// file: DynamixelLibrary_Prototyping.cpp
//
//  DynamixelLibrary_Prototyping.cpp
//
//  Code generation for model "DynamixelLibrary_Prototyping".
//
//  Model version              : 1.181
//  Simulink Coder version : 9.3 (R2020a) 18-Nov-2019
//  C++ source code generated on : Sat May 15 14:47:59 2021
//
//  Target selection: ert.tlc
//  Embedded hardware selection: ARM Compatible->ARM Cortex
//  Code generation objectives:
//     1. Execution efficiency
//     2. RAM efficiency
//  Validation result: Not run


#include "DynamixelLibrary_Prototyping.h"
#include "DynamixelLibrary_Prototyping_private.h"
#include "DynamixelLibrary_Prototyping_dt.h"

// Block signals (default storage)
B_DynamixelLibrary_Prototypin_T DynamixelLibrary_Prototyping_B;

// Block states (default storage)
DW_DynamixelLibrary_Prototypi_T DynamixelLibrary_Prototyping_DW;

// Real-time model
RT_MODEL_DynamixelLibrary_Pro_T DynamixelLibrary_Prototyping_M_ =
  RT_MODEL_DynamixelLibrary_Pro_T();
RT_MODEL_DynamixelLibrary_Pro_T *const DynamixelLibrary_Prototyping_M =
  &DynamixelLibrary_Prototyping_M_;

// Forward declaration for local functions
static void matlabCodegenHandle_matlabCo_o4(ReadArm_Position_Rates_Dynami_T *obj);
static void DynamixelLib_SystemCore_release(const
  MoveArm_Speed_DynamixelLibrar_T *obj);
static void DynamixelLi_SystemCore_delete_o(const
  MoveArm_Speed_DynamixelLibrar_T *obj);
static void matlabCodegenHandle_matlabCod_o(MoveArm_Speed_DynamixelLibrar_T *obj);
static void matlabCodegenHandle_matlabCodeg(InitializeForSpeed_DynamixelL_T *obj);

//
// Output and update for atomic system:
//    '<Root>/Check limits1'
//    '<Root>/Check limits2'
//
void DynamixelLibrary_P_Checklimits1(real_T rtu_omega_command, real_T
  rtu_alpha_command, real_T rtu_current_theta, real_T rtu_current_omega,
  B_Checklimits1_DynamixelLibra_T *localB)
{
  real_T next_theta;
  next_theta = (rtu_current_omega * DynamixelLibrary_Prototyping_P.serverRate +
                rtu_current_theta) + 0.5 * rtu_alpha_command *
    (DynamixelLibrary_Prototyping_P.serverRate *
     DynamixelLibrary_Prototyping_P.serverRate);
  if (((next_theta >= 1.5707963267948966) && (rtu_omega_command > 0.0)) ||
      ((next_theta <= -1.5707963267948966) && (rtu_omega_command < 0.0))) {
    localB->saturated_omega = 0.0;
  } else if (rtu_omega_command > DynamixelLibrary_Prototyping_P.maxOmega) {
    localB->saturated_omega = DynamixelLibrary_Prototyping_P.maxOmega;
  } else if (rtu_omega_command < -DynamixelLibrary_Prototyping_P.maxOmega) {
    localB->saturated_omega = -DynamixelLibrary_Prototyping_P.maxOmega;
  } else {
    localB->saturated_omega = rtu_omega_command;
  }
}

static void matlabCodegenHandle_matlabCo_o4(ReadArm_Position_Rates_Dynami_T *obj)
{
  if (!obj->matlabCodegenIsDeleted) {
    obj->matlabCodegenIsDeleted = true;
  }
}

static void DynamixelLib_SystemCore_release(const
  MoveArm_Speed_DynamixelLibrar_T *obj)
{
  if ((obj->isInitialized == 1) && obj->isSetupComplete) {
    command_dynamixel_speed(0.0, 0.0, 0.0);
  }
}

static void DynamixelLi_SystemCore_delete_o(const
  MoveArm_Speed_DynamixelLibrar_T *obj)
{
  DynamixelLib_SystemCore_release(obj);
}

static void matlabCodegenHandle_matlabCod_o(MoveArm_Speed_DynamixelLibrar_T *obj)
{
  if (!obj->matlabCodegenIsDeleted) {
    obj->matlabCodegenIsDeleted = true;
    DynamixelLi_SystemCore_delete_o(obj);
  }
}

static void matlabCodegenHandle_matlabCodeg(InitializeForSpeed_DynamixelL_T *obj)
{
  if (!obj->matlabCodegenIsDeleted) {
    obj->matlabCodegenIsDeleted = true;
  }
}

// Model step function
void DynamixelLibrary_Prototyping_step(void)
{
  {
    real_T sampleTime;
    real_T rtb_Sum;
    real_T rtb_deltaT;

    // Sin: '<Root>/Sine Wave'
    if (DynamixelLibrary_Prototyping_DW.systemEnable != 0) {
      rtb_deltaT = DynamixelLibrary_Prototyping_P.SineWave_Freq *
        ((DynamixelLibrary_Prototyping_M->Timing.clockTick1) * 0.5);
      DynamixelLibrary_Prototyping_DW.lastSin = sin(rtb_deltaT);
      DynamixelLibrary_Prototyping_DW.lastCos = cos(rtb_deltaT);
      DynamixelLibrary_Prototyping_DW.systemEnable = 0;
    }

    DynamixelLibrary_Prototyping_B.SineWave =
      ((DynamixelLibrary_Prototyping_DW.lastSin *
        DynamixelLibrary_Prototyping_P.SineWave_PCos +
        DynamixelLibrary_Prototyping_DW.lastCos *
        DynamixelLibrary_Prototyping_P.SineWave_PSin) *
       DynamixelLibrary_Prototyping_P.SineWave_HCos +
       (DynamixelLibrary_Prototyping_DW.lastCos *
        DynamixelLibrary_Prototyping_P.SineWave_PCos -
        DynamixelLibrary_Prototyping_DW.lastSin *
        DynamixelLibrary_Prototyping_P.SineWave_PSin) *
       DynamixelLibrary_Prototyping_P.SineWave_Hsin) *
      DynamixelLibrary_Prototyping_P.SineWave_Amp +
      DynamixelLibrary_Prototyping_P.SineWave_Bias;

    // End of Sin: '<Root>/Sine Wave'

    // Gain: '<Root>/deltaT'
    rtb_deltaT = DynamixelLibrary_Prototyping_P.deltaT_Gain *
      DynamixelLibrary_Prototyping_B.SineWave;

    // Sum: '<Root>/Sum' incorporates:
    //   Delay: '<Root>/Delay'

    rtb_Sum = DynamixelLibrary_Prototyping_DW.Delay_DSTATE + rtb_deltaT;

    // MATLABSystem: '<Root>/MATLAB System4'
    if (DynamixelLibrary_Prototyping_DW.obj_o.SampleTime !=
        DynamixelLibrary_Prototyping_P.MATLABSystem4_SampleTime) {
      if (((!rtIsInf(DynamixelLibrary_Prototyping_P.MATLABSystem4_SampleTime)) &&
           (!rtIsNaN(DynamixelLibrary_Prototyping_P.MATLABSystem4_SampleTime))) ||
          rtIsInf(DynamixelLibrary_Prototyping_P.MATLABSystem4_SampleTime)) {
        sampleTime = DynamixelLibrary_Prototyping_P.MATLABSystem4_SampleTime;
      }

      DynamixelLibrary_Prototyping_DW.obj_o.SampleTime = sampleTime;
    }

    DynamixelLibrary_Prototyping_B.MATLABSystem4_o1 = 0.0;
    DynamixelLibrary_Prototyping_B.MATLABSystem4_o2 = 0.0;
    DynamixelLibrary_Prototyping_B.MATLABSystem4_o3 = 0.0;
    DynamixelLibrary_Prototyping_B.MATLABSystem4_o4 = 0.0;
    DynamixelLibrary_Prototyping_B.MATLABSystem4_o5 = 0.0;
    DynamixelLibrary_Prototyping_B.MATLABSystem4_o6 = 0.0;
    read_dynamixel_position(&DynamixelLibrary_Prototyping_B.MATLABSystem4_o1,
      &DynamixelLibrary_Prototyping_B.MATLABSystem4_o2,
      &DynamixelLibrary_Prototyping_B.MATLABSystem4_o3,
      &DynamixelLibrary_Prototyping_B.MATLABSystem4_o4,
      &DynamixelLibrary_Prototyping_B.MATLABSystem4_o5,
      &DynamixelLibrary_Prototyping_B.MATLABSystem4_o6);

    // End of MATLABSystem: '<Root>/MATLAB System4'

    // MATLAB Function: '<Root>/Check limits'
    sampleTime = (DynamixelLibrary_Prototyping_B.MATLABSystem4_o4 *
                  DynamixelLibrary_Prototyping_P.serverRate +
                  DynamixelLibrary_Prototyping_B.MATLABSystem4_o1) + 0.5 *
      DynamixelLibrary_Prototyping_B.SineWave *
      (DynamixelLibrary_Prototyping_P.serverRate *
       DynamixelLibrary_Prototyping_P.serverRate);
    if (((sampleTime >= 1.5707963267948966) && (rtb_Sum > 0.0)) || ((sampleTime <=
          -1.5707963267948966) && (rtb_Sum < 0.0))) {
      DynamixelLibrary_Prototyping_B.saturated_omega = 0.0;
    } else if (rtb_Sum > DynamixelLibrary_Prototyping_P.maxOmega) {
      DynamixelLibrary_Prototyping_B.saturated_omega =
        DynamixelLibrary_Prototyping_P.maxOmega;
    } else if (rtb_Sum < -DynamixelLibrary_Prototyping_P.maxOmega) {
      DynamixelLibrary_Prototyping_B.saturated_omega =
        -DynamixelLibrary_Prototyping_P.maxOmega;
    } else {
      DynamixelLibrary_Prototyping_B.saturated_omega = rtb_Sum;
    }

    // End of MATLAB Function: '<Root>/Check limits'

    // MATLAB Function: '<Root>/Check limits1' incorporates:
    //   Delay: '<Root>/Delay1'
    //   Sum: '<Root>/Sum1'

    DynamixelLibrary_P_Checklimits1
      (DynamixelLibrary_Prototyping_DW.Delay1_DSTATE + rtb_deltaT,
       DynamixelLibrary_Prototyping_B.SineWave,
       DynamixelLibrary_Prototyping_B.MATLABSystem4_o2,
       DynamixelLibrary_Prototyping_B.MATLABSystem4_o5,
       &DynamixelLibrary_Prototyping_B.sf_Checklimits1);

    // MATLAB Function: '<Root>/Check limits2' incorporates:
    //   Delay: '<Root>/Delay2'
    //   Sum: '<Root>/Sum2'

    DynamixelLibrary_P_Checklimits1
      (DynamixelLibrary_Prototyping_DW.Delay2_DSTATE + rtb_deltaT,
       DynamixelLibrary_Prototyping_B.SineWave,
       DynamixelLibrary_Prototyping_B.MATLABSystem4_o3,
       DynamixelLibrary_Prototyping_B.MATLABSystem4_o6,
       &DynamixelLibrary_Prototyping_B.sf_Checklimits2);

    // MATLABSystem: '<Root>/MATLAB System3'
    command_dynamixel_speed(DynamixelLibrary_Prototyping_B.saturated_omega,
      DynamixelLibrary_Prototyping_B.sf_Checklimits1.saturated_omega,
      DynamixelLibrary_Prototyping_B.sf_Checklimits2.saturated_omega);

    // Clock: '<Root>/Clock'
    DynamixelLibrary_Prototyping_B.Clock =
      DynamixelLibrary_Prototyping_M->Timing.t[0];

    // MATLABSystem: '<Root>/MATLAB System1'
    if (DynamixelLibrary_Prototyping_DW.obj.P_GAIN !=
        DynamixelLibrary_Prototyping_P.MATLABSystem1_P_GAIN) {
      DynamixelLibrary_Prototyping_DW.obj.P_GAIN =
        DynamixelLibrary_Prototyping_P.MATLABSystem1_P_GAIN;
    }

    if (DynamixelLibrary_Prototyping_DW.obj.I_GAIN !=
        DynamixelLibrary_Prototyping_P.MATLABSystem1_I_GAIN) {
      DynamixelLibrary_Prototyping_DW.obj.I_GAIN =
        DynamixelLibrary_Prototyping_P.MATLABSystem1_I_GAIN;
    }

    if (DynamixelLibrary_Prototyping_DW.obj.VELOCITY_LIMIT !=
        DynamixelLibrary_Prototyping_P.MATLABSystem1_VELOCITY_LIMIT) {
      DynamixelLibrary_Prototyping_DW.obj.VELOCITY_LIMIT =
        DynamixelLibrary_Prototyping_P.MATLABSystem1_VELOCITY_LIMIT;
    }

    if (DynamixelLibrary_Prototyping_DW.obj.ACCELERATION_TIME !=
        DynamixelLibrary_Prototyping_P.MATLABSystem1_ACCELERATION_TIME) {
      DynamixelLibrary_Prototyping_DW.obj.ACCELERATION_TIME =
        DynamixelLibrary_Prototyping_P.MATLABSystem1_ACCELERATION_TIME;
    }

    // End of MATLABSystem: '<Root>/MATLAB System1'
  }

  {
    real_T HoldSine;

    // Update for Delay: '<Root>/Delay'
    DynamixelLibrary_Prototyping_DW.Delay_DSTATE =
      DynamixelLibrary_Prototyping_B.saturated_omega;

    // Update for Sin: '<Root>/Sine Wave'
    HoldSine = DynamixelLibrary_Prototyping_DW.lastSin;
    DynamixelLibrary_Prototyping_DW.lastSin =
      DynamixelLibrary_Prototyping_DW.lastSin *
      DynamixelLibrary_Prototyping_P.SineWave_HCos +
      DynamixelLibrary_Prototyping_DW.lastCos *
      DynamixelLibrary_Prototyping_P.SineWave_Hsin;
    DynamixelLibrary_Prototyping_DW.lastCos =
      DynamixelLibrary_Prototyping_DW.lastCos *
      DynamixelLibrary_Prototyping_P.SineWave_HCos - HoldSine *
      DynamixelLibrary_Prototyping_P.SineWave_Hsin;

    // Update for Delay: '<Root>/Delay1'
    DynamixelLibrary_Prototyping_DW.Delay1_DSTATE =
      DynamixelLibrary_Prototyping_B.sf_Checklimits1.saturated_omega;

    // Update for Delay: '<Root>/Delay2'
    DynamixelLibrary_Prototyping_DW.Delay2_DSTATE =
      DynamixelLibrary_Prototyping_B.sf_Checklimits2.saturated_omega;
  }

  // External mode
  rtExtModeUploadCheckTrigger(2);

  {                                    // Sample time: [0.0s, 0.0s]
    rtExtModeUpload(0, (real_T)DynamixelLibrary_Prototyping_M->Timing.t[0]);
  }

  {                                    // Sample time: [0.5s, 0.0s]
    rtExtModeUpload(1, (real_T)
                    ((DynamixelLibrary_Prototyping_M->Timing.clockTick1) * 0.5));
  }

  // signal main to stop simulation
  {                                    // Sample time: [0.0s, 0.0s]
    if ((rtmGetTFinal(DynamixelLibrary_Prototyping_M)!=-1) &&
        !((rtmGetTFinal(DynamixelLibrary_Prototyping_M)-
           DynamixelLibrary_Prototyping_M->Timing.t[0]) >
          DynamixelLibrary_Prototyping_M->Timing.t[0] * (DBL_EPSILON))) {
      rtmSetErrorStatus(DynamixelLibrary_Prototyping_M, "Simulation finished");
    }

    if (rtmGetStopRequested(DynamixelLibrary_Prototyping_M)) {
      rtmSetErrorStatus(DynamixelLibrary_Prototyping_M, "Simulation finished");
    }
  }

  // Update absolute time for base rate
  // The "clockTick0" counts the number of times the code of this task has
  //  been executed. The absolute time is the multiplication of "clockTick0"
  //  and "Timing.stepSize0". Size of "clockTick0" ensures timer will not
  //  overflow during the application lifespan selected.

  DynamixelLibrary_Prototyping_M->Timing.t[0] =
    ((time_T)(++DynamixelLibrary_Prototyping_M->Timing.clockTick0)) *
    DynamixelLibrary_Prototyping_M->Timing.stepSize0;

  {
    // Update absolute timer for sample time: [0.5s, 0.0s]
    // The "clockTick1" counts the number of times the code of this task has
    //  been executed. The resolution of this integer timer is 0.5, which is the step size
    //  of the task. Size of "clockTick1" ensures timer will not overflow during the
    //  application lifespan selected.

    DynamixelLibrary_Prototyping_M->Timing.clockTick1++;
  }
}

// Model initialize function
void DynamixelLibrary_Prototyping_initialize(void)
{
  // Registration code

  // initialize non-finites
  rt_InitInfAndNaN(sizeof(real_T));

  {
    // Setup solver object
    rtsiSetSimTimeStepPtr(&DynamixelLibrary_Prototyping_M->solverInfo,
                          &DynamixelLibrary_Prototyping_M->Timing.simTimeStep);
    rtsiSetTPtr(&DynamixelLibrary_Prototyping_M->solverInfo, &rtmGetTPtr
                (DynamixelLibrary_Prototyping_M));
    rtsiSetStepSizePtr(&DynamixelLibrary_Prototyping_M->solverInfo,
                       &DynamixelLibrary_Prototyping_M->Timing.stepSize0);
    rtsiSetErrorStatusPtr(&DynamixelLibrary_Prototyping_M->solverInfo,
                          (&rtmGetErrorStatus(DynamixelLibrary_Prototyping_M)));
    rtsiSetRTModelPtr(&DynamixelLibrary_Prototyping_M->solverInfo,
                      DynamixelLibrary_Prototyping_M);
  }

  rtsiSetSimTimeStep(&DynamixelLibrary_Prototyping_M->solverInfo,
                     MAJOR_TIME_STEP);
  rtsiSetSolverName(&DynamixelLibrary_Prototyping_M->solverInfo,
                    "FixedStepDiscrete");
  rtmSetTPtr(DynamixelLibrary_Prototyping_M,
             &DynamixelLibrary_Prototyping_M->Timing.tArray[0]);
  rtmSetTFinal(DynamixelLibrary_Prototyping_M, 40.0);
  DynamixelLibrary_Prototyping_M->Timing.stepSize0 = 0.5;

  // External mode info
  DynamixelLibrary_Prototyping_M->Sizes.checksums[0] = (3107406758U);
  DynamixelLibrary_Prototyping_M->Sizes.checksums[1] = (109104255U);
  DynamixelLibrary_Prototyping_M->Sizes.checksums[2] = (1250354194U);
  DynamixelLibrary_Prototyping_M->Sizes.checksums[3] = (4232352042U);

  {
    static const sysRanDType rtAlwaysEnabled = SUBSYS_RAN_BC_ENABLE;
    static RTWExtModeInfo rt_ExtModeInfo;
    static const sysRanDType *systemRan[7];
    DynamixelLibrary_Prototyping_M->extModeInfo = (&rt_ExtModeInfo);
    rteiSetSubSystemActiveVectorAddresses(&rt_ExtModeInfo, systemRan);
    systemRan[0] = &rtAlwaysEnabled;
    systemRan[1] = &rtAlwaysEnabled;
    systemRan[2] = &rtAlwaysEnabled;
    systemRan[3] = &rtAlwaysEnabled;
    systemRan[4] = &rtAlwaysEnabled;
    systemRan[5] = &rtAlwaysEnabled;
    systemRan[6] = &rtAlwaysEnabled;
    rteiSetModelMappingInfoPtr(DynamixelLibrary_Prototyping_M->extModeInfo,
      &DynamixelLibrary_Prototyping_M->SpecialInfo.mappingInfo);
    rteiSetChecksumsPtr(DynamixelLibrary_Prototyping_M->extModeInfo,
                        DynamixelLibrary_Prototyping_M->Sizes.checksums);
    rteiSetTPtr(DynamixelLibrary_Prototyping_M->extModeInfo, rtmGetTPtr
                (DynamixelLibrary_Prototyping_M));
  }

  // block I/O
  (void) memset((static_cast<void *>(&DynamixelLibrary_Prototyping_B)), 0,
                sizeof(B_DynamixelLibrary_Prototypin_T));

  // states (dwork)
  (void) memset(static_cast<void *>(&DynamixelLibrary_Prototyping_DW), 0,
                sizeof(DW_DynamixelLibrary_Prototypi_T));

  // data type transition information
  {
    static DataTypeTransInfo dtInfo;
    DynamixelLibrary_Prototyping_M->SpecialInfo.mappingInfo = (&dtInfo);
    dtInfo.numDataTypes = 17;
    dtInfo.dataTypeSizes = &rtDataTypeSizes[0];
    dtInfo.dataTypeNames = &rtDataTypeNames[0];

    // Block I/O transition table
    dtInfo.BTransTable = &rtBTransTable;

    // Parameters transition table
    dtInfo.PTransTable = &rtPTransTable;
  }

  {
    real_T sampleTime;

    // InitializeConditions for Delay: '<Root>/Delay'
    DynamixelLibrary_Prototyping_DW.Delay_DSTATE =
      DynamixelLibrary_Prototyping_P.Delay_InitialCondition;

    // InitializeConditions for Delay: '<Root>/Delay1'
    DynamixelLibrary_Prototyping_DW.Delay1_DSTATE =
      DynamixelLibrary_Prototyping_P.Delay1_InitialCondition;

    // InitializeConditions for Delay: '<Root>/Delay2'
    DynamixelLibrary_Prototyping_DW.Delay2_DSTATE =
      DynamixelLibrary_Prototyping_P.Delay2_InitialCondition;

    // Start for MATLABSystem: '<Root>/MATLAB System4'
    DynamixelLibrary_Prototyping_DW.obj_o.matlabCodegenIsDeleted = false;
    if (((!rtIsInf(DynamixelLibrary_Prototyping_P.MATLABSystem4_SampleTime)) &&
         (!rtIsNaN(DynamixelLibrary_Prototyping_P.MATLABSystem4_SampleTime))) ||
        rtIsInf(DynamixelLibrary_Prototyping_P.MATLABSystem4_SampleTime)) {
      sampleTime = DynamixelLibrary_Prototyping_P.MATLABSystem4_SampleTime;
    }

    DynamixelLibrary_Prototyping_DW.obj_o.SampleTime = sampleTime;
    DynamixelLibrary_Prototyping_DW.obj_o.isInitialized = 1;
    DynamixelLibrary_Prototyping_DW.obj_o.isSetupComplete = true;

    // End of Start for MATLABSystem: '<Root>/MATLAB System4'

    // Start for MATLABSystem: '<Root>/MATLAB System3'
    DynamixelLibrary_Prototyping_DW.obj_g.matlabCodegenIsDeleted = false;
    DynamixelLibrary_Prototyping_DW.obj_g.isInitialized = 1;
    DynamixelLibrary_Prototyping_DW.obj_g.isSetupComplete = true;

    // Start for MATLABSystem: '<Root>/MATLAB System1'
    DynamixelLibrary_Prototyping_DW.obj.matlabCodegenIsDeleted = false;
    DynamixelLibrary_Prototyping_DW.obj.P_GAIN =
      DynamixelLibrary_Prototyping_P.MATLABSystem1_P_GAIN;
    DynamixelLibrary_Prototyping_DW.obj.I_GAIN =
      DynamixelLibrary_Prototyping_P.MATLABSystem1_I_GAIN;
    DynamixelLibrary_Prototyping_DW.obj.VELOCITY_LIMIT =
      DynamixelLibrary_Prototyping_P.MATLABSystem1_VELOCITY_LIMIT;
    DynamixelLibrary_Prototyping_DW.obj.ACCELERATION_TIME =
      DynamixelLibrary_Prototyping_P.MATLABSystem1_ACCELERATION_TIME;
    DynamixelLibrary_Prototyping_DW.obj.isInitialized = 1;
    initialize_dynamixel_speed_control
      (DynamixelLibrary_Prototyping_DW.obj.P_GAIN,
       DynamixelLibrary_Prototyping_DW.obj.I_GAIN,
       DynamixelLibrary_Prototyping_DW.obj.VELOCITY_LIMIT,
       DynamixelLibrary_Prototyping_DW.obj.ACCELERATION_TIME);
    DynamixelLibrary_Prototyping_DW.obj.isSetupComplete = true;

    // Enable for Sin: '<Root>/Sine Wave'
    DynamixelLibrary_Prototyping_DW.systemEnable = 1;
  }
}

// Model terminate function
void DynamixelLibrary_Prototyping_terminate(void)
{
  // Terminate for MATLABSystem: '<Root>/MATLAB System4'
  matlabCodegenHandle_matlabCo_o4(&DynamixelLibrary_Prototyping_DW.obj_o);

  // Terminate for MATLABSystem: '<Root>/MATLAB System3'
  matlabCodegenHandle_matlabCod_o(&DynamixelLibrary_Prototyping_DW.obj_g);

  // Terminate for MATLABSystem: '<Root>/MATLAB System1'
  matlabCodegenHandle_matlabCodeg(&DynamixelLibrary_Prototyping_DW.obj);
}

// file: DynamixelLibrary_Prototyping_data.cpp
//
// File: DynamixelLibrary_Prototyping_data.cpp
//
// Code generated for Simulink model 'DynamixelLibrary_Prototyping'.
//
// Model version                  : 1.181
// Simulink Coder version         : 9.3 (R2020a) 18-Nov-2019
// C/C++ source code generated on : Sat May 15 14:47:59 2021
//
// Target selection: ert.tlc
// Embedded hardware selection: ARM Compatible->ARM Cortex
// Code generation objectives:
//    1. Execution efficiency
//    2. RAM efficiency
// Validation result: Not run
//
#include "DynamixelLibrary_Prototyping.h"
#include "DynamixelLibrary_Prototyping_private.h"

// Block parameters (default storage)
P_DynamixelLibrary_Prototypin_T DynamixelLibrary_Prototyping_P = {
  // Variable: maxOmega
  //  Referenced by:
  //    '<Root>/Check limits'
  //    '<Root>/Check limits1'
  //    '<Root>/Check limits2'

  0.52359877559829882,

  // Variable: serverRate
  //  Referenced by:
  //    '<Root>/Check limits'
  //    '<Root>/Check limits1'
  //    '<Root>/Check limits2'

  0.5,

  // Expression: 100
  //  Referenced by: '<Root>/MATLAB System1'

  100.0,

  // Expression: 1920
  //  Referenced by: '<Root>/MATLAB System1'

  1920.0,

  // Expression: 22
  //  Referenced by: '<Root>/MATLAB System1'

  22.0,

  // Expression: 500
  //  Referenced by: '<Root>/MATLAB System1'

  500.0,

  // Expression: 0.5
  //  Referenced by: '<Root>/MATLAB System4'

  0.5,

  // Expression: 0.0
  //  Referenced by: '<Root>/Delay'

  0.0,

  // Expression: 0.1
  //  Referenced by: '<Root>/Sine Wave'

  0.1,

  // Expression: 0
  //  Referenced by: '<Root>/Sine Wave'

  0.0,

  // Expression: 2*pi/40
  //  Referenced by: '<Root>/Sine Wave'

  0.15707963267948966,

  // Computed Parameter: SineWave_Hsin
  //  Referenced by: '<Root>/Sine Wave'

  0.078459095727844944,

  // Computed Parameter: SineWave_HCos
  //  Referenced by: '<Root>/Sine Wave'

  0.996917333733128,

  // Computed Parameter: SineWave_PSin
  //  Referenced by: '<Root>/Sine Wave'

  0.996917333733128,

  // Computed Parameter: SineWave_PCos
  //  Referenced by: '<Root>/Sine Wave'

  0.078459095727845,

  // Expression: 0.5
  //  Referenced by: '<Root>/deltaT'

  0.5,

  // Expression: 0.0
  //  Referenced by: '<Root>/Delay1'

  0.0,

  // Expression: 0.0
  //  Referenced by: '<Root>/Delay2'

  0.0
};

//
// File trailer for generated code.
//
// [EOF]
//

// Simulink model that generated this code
simulink model "DynamixelLibrary_Prototyping"  (R2020a)
settings: Solver=FixedStepAuto  StartTime=0.0  StopTime=40  FixedStep=0.5  RelTol=1e-3  EnableMultiTasking=on
values from neighbouring files (symbols this model uses):
  serverRate = 1/10    (= 0.1)    [Run_Initializer.m]
undefined symbols (not defined in the file or in its folder): maxOmega

== system DynamixelLibrary_Prototyping ==
  note: check if this angular rate will lead to joint limits being reached
  note: omega_t = omega_t-1 + alpha*deltaT
  Check limits : MATLAB Function  TreatAsAtomicUnit=on
  Check limits1 : MATLAB Function  TreatAsAtomicUnit=on
  Check limits2 : MATLAB Function  TreatAsAtomicUnit=on
  Clock : Clock
  Constant : Constant  Commented=on  Value=0
  Constant2 : Constant  Commented=on  Value=50
  Delay : Delay  DelayLength=1
  Delay1 : Delay  DelayLength=1
  Delay2 : Delay  DelayLength=1
  MATLAB System : MATLABSystem  Commented=on  System=InitializeForPosition  P_GAIN=400  I_GAIN=0  D_GAIN=200  MAX_POSITION=3072  MIN_POSITION=1024  VELOCITY_PROFILE=0  ACCELERATION_PROFILE=0
  MATLAB System1 : MATLABSystem  System=InitializeForSpeed  P_GAIN=100  I_GAIN=1920  VELOCITY_LIMIT=22  ACCELERATION_TIME=500
  MATLAB System10 : MATLABSystem  Commented=on  System=InitializeForSpecial  CURRENT_LIMIT=850  P_GAIN=400  I_GAIN=0  D_GAIN=200  MAX_POSITION=3072  MIN_POSITION=1024  VELOCITY_LIMIT=0
  MATLAB System11 : MATLABSystem  Commented=on  System=MoveArm_Special
  MATLAB System12 : MATLABSystem  Commented=on  System=InitializeForArmGripper  P_GAIN_ARM=400  I_GAIN_ARM=0  D_GAIN_ARM=200  P_GAIN_PROX=400  I_GAIN_PROX=0  D_GAIN_PROX=200  P_GAIN_DIST=400  I_GAIN_DIST=0  D_GAIN_DIST=200  MAX_POSITION_ARM=3072  MIN_POSITION_ARM=1024  MAX_POSITION_PROX=3072  MIN_POSITION_PROX=1024  MAX_POSITION_DIST=3072  MIN_POSITION_DIST=1024  VELOCITY_LIMIT_ARM=0  VELOCITY_LIMIT_GRIP=0  MAX_CURRENT_GRIP=1000
  MATLAB System13 : MATLABSystem  Commented=on  System=MoveArmGripper_Position
  MATLAB System2 : MATLABSystem  Commented=on  System=MoveArm_Position
  MATLAB System3 : MATLABSystem  System=MoveArm_Speed
  MATLAB System4 : MATLABSystem  System=ReadArm_Position_Rates  SampleTime=0.5
  MATLAB System5 : MATLABSystem  Commented=on  System=InitializeForPWM  PWM_LIMIT=885
  MATLAB System6 : MATLABSystem  Commented=on  System=MoveArm_PWM
  MATLAB System7 : MATLABSystem  Commented=on  System=ReadArm_Load  SampleTime=0.1
  MATLAB System8 : MATLABSystem  Commented=on  System=InitializeForTorque  CURRENT_LIMIT=850
  MATLAB System9 : MATLABSystem  Commented=on  System=MoveArm_Torque
  Sine Wave : Sin  Amplitude=0.1  Frequency=2*pi/40  Phase=pi/2  SampleTime=0.5
  Step : Step  Commented=on  Time=5  After=30  SampleTime=0
  Step1 : Step  Commented=on  Time=6  After=30  SampleTime=0
  Subtract : Sum  Commented=on  Inputs=+-
  Sum : Sum  Inputs=++|
  Sum1 : Sum  Inputs=++|
  Sum2 : Sum  Inputs=++|
  To Workspace : ToWorkspace  VariableName=theta1  SampleTime=-1
  To Workspace1 : ToWorkspace  VariableName=theta3  SampleTime=-1
  To Workspace2 : ToWorkspace  VariableName=theta2  SampleTime=-1
  To Workspace3 : ToWorkspace  VariableName=time  SampleTime=-1
  To Workspace4 : ToWorkspace  VariableName=omega1  SampleTime=-1
  To Workspace5 : ToWorkspace  VariableName=omega3  SampleTime=-1
  To Workspace6 : ToWorkspace  VariableName=omega2  SampleTime=-1
  To Workspace7 : ToWorkspace  VariableName=alpha_command  SampleTime=-1
  To Workspace8 : ToWorkspace  VariableName=omega_command  SampleTime=-1
  deltaT : Gain  Gain=0.5
  wires:
  Constant2/1 -> MATLAB System6/3, MATLAB System6/1, MATLAB System6/2
  Step/1 -> Subtract/1
  Step1/1 -> Subtract/2
  Subtract/1 -> MATLAB System9/1
  Constant/1 -> MATLAB System13/7, MATLAB System13/6, MATLAB System13/5, MATLAB System13/3, MATLAB System13/2, MATLAB System13/1, MATLAB System13/4
  MATLAB System4/1 -> Check limits/3(current_theta), To Workspace/1
  MATLAB System4/2 -> Check limits1/3(current_theta), To Workspace2/1
  MATLAB System4/3 -> To Workspace1/1, Check limits2/3(current_theta)
  Clock/1 -> To Workspace3/1
  MATLAB System4/4 -> Check limits/4(current_omega), To Workspace4/1
  MATLAB System4/5 -> Check limits1/4(current_omega), To Workspace6/1
  MATLAB System4/6 -> Check limits2/4(current_omega), To Workspace5/1
  Sine Wave/1 -> deltaT/1, Check limits2/2(alpha_command), Check limits1/2(alpha_command), Check limits/2(alpha_command), To Workspace7/1
  Check limits/1(saturated_omega) -> To Workspace8/1, Delay/1, MATLAB System3/1
  Sum/1 -> Check limits/1(omega_command)
  deltaT/1 -> Sum/2, Sum2/2, Sum1/2
  Delay/1 -> Sum/1
  Check limits1/1(saturated_omega) -> Delay1/1, MATLAB System3/2
  Check limits2/1(saturated_omega) -> Delay2/1, MATLAB System3/3
  Delay1/1 -> Sum1/1
  Delay2/1 -> Sum2/1
  Sum1/1 -> Check limits1/1(omega_command)
  Sum2/1 -> Check limits2/1(omega_command)

== matlab function DynamixelLibrary_Prototyping/Check limits1 ==
function saturated_omega = check_limits(omega_command, alpha_command, current_theta, current_omega, serverRate, maxOmega)

buffer_angle = 0; % [deg]
next_theta = current_theta + current_omega * (serverRate) + 0.5 * alpha_command * (serverRate) ^2;

if (((next_theta >= pi/2 - buffer_angle*pi/180) && (omega_command > 0)) || ((next_theta <= -pi/2 + buffer_angle*pi/180) && (omega_command < 0)))
    saturated_omega = 0;
elseif omega_command > maxOmega
    saturated_omega = maxOmega;
elseif omega_command < - maxOmega
    saturated_omega = -maxOmega;
else
    saturated_omega = omega_command;
end

== matlab function DynamixelLibrary_Prototyping/Check limits ==
function saturated_omega = check_limits(omega_command, alpha_command, current_theta, current_omega, serverRate, maxOmega)

buffer_angle = 0; % [deg]
next_theta = current_theta + current_omega * (serverRate) + 0.5 * alpha_command * (serverRate) ^2;

if (((next_theta >= pi/2 - buffer_angle*pi/180) && (omega_command > 0)) || ((next_theta <= -pi/2 + buffer_angle*pi/180) && (omega_command < 0)))
    saturated_omega = 0;
elseif omega_command > maxOmega
    saturated_omega = maxOmega;
elseif omega_command < - maxOmega
    saturated_omega = -maxOmega;
else
    saturated_omega = omega_command;
end

== matlab function DynamixelLibrary_Prototyping/Check limits2 ==
function saturated_omega = check_limits(omega_command, alpha_command, current_theta, current_omega, serverRate, maxOmega)

buffer_angle = 0; % [deg]
next_theta = current_theta + current_omega * (serverRate) + 0.5 * alpha_command * (serverRate) ^2;

if (((next_theta >= pi/2 - buffer_angle*pi/180) && (omega_command > 0)) || ((next_theta <= -pi/2 + buffer_angle*pi/180) && (omega_command < 0)))
    saturated_omega = 0;
elseif omega_command > maxOmega
    saturated_omega = maxOmega;
elseif omega_command < - maxOmega
    saturated_omega = -maxOmega;
else
    saturated_omega = omega_command;
end
